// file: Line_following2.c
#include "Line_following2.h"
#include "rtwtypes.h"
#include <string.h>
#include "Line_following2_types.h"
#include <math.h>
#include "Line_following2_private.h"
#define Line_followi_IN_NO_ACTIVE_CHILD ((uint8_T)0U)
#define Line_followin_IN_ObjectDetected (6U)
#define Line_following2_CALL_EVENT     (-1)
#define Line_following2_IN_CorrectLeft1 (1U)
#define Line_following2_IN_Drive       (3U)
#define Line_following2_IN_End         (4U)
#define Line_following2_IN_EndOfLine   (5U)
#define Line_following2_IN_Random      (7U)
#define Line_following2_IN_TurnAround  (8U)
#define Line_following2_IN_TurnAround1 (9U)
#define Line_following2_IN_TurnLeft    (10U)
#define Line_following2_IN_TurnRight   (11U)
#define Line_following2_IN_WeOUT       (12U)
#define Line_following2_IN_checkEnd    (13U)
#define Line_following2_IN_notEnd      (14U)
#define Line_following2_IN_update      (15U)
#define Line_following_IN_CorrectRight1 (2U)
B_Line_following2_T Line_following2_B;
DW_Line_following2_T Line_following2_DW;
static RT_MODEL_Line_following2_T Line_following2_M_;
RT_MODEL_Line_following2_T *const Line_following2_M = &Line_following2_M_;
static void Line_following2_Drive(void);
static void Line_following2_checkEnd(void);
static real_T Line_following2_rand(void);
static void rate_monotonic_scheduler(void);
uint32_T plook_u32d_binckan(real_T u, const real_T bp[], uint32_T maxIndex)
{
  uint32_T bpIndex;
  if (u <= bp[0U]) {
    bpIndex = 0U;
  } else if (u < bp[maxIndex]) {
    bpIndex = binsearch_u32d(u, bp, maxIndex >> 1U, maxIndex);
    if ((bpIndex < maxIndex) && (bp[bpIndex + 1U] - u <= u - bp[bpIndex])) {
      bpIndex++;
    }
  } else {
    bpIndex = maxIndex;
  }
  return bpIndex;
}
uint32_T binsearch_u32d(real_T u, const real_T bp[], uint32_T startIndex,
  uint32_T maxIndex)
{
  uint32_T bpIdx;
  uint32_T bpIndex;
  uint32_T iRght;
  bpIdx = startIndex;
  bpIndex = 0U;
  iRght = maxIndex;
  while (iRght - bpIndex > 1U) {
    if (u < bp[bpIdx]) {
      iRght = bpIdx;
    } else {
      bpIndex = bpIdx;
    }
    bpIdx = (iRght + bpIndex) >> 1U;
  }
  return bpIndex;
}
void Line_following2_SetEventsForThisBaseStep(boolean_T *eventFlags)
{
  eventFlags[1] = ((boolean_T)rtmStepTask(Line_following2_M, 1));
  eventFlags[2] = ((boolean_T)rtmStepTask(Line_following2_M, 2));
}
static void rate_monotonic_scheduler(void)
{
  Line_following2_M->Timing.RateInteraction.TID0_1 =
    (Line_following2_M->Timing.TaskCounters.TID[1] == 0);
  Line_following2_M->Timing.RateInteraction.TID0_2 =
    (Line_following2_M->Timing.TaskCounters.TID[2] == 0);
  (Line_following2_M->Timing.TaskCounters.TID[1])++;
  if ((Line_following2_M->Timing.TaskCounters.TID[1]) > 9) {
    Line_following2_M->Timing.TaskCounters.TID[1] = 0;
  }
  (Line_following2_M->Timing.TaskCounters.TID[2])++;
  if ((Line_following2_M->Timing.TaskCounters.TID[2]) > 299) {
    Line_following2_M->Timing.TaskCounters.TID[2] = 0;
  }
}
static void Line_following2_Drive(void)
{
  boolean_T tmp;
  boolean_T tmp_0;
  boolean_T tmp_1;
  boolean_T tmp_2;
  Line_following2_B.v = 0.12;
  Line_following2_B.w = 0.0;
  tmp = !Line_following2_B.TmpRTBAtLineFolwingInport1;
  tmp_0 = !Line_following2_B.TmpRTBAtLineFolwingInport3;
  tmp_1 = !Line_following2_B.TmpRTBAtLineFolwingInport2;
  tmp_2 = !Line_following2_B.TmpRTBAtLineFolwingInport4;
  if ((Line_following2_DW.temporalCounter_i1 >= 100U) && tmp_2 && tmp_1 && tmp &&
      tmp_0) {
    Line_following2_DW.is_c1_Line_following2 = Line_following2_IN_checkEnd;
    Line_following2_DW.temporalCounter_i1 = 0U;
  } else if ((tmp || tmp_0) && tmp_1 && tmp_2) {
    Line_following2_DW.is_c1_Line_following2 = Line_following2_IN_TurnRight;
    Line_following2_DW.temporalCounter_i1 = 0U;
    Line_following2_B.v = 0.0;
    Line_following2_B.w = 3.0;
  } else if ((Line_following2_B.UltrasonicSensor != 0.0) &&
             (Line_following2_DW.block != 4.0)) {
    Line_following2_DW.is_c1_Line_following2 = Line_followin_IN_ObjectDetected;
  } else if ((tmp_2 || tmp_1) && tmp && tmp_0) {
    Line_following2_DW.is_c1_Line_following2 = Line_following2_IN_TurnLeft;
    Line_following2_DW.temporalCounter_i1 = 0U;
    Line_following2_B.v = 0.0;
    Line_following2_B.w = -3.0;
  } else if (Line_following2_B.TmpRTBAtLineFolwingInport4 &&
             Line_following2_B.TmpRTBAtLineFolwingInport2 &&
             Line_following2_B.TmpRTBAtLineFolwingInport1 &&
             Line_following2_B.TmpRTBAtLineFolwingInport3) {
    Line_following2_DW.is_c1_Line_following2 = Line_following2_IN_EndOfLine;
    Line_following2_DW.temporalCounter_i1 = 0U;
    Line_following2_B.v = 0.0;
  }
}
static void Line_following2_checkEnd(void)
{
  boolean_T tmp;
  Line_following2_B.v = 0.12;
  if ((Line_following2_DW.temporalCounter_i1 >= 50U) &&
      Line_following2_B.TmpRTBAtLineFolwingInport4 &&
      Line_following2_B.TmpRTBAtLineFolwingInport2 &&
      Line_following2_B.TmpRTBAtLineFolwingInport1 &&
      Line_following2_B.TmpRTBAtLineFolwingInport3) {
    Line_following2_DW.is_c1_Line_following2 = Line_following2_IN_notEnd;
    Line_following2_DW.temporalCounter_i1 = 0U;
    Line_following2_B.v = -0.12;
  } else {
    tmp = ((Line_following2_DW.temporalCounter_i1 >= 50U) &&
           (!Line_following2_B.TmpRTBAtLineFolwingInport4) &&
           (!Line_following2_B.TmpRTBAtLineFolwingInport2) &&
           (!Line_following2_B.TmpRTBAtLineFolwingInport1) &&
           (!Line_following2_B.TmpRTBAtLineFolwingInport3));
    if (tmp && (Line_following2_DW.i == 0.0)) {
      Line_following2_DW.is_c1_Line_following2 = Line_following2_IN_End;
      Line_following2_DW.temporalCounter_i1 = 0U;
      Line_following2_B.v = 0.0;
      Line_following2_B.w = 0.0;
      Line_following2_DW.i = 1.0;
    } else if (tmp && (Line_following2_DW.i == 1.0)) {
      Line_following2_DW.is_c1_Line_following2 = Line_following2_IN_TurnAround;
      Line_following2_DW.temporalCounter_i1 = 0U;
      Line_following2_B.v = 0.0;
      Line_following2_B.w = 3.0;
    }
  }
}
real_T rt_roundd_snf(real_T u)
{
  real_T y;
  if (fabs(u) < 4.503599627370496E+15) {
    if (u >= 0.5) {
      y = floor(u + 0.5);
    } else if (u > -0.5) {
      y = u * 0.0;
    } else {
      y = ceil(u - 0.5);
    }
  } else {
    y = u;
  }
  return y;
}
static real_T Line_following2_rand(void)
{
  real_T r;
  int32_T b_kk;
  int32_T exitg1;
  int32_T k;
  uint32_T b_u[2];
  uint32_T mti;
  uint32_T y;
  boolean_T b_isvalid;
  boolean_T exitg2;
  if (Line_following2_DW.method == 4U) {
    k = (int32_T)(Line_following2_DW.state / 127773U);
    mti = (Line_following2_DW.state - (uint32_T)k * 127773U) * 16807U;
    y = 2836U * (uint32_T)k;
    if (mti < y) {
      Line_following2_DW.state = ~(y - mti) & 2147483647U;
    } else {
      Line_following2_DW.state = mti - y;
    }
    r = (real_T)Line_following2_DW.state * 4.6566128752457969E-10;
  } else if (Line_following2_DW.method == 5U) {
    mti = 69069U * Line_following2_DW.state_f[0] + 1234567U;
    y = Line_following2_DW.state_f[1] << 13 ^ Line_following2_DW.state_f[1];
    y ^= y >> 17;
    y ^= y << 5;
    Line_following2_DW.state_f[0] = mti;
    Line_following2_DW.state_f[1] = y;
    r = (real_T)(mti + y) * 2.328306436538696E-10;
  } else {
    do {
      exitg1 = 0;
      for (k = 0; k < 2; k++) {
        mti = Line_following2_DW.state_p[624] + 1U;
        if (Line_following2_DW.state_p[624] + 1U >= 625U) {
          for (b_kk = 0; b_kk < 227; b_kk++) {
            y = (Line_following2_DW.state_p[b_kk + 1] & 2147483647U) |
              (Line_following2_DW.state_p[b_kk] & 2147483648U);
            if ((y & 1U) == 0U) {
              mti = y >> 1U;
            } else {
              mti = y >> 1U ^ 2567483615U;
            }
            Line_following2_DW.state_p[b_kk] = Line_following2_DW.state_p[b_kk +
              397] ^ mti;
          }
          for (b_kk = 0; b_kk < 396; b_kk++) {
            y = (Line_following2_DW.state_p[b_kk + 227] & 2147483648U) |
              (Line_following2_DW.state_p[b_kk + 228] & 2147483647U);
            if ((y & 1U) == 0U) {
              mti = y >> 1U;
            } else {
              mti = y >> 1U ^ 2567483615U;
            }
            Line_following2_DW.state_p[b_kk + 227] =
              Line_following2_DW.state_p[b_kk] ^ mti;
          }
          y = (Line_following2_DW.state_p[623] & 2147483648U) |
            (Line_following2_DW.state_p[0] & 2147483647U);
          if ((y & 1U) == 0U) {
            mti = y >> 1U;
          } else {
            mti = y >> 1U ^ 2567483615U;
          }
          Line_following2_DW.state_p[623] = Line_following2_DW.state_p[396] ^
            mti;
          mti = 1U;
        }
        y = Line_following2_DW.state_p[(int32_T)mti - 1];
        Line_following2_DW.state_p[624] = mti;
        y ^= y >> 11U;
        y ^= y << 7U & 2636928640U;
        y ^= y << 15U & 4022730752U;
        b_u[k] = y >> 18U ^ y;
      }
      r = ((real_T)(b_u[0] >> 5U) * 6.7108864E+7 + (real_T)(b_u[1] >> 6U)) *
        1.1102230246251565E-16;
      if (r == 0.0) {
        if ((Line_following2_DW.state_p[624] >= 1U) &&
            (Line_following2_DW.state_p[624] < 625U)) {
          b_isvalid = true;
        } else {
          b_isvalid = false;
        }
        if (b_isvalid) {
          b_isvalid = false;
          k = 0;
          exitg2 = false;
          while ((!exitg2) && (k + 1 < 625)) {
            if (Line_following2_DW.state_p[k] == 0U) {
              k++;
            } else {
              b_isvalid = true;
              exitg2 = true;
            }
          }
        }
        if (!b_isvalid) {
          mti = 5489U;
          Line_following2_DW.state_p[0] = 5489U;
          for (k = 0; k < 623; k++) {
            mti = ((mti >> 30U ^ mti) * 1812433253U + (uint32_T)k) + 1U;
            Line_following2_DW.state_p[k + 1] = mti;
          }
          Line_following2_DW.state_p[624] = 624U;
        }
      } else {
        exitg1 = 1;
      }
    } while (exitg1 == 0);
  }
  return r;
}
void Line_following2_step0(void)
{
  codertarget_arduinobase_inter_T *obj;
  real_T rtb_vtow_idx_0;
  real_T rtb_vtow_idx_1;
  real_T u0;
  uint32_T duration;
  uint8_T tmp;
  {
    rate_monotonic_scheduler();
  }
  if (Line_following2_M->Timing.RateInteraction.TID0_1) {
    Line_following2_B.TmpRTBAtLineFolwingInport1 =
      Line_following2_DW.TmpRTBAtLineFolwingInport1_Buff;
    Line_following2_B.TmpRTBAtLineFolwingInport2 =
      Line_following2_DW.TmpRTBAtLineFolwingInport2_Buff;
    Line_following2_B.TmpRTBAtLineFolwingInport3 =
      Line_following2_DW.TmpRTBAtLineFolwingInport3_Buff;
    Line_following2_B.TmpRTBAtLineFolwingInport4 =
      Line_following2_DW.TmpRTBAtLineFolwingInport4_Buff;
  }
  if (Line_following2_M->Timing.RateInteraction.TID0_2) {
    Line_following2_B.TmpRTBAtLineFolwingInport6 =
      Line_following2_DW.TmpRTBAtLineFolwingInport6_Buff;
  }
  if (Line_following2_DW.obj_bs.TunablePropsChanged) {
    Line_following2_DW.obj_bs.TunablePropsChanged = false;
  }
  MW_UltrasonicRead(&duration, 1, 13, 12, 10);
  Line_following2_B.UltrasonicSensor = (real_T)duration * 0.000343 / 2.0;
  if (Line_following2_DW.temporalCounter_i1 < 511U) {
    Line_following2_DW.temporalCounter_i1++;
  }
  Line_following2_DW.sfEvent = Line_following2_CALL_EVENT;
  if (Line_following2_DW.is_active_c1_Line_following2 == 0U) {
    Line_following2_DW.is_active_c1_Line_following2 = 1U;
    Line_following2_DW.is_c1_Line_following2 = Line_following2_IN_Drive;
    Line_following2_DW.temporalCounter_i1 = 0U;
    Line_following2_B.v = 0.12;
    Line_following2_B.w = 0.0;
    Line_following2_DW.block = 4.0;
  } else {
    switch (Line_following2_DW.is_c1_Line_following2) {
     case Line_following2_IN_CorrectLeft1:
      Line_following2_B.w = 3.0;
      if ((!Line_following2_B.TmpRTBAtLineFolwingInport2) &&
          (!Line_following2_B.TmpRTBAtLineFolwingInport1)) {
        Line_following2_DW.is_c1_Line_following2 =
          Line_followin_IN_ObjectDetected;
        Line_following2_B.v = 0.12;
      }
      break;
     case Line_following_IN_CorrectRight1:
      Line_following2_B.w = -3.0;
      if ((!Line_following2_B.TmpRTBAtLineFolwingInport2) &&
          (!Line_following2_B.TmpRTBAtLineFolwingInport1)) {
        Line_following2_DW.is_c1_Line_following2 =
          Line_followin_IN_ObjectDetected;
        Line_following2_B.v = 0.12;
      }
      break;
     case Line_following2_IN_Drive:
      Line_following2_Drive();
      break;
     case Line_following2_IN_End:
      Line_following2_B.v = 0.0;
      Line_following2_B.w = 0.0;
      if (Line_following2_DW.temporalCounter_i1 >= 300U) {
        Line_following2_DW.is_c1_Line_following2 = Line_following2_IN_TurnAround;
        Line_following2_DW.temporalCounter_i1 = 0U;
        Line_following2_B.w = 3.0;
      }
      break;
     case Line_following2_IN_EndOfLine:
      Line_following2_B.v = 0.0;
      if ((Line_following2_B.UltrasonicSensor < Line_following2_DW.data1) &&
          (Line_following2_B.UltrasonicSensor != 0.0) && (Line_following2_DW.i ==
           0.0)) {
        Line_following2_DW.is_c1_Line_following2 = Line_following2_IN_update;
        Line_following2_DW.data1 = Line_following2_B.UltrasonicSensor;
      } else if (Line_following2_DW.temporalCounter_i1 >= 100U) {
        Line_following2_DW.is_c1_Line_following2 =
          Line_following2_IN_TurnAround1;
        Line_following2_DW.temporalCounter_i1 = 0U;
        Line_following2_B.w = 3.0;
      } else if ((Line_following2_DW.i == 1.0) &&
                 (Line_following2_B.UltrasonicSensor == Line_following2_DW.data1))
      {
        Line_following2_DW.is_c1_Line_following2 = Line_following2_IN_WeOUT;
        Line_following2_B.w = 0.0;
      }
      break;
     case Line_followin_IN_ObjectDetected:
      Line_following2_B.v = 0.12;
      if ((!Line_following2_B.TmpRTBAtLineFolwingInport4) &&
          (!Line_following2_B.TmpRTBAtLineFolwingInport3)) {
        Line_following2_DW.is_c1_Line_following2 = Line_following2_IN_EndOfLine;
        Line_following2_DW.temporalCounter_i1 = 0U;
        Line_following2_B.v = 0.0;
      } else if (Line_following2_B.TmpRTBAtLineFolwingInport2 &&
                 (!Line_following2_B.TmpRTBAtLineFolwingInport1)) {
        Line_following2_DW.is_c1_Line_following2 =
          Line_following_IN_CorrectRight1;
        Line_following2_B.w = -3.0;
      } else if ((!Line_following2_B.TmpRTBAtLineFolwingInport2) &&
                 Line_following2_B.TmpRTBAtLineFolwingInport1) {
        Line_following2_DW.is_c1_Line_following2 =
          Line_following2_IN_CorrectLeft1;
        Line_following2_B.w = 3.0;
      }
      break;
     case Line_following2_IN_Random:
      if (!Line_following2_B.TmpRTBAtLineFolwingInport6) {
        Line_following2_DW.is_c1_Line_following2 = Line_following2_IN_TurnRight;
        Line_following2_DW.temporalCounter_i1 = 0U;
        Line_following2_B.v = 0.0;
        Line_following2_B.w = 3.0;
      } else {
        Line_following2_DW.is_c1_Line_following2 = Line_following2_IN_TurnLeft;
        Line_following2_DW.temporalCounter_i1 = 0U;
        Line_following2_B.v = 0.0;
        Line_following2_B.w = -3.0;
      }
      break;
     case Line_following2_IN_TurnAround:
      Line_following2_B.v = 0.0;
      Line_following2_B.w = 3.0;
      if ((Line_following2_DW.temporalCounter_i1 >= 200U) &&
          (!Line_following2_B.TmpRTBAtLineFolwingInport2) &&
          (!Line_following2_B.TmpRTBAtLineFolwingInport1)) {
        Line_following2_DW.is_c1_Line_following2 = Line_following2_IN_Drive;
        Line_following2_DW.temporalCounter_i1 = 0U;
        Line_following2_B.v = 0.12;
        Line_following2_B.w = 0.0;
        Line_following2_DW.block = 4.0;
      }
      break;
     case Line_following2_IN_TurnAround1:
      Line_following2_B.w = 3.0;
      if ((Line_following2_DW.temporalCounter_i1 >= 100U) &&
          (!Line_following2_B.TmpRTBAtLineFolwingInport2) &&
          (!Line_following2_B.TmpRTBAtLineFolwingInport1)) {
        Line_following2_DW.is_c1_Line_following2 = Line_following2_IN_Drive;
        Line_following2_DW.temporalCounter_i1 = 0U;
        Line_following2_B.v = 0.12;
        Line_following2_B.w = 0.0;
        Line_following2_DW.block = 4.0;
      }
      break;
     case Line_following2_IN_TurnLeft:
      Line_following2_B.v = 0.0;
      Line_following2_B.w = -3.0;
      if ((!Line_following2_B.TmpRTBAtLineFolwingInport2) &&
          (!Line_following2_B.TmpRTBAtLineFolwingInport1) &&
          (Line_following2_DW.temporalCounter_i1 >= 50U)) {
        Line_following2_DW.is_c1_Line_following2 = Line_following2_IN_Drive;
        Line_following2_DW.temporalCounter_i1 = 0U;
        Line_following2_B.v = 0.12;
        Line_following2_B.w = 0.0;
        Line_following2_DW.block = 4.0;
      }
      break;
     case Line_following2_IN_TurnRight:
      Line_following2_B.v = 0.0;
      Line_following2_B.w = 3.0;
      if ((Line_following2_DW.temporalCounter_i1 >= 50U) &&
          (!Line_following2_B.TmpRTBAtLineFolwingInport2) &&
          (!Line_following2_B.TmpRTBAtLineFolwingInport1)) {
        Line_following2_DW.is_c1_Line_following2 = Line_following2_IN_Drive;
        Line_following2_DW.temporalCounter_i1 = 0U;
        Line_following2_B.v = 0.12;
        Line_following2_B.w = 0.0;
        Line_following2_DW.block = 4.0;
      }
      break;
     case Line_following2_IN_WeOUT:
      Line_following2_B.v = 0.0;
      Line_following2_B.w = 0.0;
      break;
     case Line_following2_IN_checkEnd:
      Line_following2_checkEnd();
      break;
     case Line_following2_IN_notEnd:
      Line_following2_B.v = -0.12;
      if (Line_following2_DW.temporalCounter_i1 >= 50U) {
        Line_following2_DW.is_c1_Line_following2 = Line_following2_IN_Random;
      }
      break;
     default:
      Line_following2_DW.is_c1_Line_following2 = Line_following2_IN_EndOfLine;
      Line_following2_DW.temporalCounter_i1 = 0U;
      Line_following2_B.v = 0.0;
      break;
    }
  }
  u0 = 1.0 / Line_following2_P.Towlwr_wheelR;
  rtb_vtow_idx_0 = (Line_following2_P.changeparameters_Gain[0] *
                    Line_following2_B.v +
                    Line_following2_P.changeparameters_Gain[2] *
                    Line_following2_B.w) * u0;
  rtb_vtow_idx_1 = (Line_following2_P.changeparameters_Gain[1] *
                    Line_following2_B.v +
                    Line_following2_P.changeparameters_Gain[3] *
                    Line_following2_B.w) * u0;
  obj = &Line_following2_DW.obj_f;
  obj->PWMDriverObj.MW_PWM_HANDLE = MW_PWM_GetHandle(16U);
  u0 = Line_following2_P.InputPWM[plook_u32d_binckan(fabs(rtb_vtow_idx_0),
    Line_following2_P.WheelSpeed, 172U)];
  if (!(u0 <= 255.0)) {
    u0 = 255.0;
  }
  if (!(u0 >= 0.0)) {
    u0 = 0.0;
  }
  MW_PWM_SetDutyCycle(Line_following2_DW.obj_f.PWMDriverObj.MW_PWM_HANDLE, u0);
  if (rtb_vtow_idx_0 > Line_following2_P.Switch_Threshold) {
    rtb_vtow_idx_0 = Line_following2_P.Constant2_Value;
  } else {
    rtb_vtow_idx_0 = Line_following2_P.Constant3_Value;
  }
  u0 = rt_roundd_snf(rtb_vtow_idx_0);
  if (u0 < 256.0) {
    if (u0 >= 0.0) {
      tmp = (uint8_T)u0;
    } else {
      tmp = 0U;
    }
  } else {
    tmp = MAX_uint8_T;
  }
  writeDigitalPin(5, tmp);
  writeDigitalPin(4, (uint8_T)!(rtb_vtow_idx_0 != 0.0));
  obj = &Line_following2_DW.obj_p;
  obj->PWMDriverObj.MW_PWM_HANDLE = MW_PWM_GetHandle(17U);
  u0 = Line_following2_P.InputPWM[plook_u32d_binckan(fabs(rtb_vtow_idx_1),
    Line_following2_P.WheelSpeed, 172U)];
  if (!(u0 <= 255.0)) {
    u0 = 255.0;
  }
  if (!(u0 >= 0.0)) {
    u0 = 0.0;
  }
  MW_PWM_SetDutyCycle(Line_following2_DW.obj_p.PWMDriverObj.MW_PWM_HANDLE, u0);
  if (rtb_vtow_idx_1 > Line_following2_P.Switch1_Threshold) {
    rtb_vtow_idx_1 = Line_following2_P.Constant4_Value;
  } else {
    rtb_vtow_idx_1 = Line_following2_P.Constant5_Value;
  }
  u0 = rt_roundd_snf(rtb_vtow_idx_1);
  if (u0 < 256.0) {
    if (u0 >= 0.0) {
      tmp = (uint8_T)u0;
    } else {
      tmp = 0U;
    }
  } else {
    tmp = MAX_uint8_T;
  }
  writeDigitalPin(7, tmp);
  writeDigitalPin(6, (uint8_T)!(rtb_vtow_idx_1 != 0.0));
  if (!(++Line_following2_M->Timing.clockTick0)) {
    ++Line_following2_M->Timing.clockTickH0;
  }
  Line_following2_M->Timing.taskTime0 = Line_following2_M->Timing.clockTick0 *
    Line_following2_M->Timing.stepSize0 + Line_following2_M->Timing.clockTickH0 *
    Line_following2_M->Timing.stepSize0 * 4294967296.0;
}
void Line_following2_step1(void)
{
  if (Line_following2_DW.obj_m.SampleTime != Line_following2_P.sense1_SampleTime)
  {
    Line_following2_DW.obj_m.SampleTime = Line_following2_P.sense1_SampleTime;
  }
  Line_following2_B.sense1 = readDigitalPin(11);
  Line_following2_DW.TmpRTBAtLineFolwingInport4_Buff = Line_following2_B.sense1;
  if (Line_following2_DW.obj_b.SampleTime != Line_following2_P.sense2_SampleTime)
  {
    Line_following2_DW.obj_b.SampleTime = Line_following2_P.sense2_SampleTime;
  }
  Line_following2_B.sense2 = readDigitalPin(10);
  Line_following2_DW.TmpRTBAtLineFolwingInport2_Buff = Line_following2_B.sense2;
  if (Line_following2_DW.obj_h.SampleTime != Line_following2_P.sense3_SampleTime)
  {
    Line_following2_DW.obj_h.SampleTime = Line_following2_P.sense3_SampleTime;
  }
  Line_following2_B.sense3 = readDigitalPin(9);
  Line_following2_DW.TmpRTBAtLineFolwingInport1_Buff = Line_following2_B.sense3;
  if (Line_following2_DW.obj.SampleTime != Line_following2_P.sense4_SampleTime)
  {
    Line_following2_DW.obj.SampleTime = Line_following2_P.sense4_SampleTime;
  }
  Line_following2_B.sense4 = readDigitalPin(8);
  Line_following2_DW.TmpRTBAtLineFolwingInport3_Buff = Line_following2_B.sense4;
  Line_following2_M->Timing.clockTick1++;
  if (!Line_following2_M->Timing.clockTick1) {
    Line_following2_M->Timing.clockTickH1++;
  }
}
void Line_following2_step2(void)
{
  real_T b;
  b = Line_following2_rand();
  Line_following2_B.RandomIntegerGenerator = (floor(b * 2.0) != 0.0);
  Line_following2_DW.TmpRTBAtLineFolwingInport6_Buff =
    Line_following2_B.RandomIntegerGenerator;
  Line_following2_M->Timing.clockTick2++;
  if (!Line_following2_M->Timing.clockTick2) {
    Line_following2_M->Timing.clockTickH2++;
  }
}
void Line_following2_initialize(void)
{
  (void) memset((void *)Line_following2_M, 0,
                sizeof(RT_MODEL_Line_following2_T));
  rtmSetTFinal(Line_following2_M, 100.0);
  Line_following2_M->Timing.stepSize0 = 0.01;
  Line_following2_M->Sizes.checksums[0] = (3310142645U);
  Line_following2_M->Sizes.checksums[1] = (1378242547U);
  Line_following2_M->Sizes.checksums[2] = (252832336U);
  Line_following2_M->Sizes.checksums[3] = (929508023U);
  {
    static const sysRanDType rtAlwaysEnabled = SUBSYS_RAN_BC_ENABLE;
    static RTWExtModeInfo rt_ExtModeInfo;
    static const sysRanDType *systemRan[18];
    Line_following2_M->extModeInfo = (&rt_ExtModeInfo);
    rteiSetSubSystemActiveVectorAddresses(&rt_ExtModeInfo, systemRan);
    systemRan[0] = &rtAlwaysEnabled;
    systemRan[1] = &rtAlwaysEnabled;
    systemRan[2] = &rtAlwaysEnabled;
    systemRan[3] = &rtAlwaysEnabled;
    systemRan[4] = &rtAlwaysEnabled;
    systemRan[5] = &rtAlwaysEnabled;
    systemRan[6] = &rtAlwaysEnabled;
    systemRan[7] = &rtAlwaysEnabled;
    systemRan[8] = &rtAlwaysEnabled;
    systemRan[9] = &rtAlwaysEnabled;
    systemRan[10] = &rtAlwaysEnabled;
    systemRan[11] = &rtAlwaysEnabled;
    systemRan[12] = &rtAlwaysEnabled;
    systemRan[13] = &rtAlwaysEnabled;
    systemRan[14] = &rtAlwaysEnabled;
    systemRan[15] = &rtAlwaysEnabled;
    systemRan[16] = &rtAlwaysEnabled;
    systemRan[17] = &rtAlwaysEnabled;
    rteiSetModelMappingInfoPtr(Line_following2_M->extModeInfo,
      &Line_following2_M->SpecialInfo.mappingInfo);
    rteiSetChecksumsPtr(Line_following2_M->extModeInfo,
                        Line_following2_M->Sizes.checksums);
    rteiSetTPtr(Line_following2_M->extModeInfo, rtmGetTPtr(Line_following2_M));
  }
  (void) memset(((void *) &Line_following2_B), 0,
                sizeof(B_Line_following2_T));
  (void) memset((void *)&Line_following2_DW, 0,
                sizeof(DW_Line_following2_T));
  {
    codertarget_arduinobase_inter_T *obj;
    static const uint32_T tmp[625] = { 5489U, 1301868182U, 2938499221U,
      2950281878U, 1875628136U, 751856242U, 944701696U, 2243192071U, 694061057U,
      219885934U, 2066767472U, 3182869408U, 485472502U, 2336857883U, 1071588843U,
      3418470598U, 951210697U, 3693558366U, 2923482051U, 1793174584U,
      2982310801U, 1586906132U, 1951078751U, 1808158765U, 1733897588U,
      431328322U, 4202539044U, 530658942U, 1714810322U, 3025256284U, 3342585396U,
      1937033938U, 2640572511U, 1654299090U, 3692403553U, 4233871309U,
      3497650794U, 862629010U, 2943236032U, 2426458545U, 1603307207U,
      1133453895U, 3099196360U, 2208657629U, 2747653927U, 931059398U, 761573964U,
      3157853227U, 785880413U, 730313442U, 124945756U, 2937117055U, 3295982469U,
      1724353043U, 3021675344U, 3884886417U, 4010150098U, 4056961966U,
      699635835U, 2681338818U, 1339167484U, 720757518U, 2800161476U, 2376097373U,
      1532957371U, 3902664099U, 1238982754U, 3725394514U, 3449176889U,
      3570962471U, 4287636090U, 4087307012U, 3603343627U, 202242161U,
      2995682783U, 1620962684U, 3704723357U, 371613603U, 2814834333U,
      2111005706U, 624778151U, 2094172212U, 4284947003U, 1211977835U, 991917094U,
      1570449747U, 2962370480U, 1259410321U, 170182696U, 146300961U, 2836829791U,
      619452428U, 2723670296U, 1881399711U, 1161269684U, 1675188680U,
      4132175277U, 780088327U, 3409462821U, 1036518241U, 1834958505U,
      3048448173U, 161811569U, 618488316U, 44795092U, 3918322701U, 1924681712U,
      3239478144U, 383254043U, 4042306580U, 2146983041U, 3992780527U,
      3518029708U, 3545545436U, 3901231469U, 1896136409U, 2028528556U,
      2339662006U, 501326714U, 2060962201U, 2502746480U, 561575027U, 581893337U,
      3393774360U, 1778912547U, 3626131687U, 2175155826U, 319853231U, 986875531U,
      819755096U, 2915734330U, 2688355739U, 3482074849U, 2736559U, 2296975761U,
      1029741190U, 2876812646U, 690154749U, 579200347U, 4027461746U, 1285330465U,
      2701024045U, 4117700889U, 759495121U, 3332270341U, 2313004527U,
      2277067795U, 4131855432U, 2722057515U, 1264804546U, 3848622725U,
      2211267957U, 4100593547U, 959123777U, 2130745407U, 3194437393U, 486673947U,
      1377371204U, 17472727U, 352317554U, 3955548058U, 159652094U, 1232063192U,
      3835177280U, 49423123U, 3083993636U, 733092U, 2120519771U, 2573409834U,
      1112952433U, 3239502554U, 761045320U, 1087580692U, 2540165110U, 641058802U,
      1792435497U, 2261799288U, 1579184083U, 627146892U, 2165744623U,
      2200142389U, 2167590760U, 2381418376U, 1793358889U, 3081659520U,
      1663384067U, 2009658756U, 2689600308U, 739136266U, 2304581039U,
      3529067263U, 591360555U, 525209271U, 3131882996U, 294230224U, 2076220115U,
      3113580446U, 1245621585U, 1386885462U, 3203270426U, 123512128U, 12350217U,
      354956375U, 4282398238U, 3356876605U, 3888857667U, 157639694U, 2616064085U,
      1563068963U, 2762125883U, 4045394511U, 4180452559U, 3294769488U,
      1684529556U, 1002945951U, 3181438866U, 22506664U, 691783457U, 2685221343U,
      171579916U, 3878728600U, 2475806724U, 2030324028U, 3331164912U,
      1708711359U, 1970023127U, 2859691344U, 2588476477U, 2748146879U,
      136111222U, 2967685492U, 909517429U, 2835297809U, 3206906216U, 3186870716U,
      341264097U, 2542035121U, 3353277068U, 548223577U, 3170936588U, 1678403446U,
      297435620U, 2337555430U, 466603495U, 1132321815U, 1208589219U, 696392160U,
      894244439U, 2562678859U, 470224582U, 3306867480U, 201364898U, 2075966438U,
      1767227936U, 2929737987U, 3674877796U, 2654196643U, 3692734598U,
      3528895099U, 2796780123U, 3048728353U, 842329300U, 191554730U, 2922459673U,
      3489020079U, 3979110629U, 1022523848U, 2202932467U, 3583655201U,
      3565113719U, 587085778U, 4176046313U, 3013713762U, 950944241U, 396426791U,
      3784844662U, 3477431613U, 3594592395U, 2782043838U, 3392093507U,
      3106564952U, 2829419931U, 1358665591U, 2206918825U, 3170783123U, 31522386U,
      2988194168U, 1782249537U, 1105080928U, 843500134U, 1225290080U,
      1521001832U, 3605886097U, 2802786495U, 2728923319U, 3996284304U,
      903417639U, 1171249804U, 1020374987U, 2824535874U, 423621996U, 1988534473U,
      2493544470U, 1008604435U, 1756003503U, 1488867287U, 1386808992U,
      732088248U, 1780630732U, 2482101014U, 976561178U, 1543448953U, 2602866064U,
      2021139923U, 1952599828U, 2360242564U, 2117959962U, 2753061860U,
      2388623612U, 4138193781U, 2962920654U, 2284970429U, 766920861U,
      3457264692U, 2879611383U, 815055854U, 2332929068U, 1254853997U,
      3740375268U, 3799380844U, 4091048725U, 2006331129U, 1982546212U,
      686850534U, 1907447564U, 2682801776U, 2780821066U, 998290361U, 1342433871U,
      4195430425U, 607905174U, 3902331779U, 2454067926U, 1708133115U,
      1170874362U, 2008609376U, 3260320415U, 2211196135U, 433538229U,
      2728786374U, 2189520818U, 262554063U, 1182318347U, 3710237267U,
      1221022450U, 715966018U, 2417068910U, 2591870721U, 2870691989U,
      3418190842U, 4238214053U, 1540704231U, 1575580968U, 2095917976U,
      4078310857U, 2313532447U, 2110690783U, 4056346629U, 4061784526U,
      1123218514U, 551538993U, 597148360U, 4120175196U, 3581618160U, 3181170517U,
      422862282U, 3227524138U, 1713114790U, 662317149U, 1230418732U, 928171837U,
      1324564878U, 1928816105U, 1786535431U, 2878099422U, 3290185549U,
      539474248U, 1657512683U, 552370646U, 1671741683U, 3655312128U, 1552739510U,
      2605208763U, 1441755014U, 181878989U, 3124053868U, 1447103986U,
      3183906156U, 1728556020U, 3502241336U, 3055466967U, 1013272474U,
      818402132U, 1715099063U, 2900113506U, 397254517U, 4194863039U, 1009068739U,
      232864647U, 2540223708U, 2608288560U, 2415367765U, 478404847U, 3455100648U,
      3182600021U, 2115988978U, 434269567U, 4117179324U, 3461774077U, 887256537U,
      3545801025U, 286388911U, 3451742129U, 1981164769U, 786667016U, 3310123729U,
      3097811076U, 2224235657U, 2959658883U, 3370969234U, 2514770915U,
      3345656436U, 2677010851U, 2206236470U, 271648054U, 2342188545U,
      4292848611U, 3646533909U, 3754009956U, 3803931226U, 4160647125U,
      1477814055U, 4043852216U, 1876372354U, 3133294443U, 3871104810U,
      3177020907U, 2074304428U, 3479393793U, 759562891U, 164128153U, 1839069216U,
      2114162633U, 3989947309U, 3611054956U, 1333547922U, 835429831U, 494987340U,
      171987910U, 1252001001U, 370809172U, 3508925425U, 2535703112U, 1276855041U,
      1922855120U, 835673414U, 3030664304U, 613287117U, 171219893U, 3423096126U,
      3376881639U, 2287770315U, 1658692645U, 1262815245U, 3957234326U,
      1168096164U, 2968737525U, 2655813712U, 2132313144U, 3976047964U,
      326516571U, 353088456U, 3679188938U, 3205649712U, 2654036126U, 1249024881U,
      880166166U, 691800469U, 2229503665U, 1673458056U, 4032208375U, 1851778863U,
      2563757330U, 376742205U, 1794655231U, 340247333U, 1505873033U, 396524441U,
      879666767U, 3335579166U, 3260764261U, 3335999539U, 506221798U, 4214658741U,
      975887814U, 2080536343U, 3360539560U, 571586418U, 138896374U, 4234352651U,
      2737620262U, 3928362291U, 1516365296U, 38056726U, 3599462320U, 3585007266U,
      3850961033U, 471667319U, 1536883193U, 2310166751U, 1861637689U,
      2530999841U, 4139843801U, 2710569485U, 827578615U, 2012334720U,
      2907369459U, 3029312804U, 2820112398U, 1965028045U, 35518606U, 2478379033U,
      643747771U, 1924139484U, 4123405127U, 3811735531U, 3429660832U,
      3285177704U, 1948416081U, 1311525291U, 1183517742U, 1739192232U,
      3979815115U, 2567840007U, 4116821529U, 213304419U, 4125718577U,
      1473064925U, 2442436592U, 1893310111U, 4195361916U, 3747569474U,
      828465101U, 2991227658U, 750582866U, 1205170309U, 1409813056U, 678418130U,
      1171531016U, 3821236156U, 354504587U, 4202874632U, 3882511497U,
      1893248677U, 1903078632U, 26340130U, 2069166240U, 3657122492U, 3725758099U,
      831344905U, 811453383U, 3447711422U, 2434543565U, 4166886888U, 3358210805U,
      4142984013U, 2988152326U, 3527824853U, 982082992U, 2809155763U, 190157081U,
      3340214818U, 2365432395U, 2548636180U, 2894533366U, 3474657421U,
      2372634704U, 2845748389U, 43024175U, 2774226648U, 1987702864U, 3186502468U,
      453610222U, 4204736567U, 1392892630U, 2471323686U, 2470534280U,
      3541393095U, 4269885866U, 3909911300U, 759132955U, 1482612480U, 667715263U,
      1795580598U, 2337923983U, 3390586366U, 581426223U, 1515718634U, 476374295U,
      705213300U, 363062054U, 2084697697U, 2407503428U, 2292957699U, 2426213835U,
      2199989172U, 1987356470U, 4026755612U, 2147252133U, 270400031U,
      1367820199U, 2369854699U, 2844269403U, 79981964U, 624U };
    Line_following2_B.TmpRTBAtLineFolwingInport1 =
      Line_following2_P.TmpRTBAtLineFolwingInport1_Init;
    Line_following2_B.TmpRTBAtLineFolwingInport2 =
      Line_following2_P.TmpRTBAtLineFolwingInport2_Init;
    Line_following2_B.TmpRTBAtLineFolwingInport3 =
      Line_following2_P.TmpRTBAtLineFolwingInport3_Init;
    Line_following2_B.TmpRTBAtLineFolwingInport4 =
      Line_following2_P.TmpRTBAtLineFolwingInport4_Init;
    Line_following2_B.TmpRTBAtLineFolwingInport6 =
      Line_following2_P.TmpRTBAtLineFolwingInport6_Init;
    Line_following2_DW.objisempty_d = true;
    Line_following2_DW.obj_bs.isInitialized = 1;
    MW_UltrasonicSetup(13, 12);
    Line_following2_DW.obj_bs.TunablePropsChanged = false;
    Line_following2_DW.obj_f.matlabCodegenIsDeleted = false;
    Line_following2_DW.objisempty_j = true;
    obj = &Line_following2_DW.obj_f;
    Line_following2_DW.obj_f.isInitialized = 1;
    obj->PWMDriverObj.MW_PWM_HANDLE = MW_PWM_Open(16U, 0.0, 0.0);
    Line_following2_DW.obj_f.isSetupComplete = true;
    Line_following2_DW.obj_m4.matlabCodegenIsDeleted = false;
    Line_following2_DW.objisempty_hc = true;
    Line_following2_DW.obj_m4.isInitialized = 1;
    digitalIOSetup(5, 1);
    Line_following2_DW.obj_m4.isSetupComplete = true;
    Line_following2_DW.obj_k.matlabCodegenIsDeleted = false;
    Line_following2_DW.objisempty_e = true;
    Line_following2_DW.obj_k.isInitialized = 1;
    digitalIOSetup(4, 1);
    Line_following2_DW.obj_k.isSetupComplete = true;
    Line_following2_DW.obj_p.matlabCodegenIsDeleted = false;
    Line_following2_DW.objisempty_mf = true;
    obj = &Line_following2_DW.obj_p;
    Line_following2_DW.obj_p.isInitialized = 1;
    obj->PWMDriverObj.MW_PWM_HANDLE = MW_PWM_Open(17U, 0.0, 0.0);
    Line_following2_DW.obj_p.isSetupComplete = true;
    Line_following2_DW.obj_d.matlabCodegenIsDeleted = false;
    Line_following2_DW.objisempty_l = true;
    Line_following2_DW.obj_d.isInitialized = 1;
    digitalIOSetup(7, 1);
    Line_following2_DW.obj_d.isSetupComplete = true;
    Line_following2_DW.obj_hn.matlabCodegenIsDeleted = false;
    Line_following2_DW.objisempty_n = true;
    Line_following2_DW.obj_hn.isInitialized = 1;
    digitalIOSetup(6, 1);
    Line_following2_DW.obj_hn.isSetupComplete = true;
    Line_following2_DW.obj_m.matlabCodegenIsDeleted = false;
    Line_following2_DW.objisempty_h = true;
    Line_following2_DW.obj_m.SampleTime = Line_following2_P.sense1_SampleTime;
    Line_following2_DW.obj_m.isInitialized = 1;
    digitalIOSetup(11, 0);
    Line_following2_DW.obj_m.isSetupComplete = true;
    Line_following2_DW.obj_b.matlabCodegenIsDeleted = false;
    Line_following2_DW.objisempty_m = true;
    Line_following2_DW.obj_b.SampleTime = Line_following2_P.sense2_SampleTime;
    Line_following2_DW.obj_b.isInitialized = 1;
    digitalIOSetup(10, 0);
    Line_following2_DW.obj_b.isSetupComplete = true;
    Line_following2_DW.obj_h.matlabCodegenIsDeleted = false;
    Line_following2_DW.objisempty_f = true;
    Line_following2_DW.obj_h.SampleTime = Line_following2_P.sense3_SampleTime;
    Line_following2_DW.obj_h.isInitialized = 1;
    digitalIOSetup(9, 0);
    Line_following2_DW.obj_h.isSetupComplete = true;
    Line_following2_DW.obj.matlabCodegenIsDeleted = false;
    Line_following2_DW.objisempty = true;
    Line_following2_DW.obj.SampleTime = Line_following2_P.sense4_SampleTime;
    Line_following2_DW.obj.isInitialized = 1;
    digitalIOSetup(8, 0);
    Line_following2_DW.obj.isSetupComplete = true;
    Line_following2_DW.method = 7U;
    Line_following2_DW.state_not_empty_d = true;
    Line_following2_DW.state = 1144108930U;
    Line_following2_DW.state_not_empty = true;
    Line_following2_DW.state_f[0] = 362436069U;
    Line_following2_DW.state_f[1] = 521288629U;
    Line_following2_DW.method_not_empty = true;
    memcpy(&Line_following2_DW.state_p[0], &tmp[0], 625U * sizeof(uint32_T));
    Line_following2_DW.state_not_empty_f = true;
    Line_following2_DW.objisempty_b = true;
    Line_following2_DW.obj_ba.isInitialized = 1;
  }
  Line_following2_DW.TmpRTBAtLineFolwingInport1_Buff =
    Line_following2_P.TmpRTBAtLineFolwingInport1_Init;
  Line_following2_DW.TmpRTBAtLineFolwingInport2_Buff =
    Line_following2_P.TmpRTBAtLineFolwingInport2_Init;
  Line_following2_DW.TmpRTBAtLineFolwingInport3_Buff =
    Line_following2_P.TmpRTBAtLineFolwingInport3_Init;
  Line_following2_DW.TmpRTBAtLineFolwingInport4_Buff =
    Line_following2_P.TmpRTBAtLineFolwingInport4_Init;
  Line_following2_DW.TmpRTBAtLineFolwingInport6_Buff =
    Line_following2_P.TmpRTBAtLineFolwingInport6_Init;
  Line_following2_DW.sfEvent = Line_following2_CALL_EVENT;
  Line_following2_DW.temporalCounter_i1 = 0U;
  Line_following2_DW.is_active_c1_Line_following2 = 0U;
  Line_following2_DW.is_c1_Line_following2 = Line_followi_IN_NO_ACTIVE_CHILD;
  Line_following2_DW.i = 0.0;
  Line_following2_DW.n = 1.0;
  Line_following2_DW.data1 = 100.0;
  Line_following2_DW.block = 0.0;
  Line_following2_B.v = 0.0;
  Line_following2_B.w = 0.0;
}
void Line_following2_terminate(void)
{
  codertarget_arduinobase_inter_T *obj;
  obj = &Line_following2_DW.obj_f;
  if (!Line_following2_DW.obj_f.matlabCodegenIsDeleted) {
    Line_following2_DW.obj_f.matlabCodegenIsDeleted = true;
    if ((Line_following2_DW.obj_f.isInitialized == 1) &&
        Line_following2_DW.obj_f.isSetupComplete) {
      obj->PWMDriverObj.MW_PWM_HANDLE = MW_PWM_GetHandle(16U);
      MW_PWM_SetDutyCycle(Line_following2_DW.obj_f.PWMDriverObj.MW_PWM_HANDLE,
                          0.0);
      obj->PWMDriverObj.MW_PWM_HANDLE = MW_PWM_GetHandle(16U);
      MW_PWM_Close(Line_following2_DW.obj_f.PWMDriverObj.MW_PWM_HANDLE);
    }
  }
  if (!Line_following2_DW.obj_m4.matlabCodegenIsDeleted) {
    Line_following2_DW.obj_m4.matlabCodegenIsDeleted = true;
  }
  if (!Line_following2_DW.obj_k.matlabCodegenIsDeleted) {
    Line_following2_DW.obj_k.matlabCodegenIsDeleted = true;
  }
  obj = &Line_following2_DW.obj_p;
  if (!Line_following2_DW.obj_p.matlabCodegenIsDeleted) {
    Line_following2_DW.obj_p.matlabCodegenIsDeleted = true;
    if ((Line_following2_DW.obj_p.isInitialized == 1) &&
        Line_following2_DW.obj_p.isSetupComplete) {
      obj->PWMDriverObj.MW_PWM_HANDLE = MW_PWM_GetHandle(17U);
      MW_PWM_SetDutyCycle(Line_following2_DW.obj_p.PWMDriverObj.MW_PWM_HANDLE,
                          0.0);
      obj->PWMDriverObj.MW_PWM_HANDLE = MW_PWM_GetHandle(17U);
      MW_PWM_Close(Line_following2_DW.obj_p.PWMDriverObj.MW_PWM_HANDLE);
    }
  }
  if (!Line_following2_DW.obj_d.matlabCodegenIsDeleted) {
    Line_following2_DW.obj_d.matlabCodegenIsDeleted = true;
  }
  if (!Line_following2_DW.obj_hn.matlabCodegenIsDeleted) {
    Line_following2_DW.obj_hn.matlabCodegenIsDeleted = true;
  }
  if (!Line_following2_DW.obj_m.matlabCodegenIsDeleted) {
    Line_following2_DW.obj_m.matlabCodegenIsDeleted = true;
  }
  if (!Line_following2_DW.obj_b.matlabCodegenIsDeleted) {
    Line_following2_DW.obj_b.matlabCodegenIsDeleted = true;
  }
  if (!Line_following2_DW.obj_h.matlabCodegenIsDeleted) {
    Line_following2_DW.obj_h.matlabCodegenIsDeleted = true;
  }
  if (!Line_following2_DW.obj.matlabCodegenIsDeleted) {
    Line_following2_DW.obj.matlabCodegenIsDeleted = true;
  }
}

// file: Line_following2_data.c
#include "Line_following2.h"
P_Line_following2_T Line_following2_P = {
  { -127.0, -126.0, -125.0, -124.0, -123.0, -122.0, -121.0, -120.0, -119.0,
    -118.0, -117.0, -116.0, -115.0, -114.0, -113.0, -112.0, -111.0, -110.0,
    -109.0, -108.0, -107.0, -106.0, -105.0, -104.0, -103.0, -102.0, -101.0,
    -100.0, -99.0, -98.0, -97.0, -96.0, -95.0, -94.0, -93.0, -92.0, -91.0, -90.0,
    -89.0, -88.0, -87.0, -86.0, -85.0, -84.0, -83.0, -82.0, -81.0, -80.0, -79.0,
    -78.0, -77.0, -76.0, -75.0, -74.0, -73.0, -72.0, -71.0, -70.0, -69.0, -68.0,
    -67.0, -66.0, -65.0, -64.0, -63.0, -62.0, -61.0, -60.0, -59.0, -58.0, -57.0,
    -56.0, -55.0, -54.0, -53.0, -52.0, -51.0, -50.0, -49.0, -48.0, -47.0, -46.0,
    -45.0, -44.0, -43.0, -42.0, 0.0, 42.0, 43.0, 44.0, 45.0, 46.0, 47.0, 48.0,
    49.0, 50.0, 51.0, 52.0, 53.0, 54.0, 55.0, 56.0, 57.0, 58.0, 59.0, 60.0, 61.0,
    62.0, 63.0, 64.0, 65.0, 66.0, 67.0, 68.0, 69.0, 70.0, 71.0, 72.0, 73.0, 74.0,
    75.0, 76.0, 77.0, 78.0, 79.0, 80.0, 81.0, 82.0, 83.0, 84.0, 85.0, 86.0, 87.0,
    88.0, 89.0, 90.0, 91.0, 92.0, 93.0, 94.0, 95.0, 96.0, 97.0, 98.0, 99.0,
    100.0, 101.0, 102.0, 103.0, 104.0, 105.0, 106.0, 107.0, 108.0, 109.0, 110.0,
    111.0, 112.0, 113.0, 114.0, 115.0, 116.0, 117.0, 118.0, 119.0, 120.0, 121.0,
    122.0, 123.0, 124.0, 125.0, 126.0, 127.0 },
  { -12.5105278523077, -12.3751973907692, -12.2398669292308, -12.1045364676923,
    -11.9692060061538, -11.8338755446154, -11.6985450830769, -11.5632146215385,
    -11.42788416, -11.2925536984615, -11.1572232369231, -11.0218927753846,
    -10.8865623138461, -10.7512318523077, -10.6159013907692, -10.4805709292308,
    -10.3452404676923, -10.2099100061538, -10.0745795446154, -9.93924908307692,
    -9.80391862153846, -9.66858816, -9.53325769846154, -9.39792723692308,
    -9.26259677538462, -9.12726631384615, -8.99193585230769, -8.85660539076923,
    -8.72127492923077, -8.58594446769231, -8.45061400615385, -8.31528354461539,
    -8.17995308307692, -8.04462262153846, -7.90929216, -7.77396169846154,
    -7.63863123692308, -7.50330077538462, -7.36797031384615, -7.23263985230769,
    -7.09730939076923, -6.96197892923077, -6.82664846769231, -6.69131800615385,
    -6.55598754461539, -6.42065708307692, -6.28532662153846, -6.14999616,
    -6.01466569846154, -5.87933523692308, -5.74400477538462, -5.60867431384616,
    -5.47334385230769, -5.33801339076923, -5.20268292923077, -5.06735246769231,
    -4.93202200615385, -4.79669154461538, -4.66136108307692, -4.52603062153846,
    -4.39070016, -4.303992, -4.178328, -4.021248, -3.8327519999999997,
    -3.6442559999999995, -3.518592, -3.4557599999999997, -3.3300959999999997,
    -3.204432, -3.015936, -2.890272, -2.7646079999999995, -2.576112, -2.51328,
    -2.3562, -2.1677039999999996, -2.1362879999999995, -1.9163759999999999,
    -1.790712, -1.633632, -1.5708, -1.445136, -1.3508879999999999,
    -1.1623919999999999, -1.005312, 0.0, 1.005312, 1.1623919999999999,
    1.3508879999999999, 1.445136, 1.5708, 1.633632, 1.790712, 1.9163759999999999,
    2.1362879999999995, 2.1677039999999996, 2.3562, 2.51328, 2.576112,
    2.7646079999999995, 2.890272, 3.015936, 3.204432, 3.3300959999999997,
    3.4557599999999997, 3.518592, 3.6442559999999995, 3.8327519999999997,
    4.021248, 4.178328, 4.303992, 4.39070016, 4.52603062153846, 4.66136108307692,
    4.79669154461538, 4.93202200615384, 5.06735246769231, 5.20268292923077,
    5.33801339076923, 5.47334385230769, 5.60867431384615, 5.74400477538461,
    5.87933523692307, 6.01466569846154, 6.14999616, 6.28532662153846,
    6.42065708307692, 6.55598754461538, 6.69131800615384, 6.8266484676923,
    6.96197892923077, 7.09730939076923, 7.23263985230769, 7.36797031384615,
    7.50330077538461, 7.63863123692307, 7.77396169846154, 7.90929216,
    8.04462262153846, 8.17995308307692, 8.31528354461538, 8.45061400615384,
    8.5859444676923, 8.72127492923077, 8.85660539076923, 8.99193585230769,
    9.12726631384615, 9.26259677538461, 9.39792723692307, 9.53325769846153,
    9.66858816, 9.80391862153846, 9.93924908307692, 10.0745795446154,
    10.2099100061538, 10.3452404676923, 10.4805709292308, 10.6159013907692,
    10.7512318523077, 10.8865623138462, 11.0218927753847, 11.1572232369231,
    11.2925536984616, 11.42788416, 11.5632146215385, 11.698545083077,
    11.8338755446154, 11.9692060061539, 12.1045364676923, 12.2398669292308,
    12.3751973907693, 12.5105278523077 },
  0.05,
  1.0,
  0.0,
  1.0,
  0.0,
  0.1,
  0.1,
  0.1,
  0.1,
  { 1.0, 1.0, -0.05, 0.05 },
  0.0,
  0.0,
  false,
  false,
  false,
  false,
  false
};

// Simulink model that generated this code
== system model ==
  PWM#1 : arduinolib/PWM  pinNumber=16  <- 1: Lookup_nD#1
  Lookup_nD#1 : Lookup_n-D  BreakpointsForDimension1=WheelSpeed  Table=InputPWM  InterpMethod=Nearest  <- 1: Abs#1
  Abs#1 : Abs  <- 1: Towlwr
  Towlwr : mobileRoboticsTrainingLib/To wlwr  <- 1: Stateflowchart#1, 2: Stateflowchart#1/2
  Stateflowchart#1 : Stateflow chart  <- 1: sense3, 2: sense2, 3: sense4, 4: sense1, 5: UltrasonicSensor, 6: RandomIntegerGenerator
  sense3 : arduinolib/Digital Input  pinNumber=9
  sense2 : arduinolib/Digital Input  pinNumber=10
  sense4 : arduinolib/Digital Input  pinNumber=8
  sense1 : arduinolib/Digital Input  pinNumber=11
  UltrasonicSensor : arduinosensorlib/Ultrasonic Sensor
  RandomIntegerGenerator : commrandsrc3/Random Integer Generator
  DigitalOutput#1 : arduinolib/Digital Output  pinNumber=5  <- 1: Switch
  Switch : Switch  Criteria=u2 > Threshold  <- 1: Constant2, 2: Towlwr, 3: Constant3
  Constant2 : Constant
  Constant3 : Constant  Value=0
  DigitalOutput#2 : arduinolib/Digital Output  pinNumber=4  <- 1: Logic#1
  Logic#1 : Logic  Operator=NOT  <- 1: Switch
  PWM#2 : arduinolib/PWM  pinNumber=17  <- 1: Lookup_nD#2
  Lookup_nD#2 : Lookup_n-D  BreakpointsForDimension1=WheelSpeed  Table=InputPWM  InterpMethod=Nearest  <- 1: Abs#2
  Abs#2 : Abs  <- 1: Towlwr/2
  DigitalOutput#3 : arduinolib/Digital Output  pinNumber=7  <- 1: Switch1
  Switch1 : Switch  Criteria=u2 > Threshold  <- 1: Constant4, 2: Towlwr/2, 3: Constant5
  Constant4 : Constant
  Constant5 : Constant  Value=0
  DigitalOutput#4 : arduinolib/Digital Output  pinNumber=6  <- 1: Logic#2
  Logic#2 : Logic  Operator=NOT  <- 1: Switch1
== stateflow chart Stateflowchart#1 ==
  state Random
    entry:
    dir;
  state notEnd
    entry:
    v=-0.12;
  state End
    entry:
    v=0;
    w=0;
    i=1;
  state TurnAround
    entry:
    v=0;
    w=3;
  state checkEnd
    entry:
    v=0.12;
  state TurnLeft
    entry:
    v=0;
    w=-3;
  state TurnRight
    entry:
    v=0;
    w=3;
  state Drive
    entry:
    v=0.12;
    w=0;
    i;
    n;
    data1;
    block=4;
  state ObjectDetected
    entry:
    v=0.12;
  state CorrectRight1
    entry:
    w=-3;
  state TurnAround1
    entry:
    w=3;
  state CorrectLeft1
    entry:
    w=3;
  state EndOfLine
    entry:
    v=0;
  state update
    entry:
    data1=ultraSonic;
  state WeOUT
    entry:
    v=0;
    w=0;
  checkEnd -> TurnAround [order 3] : [after(0.5,sec) &&sense1 ==0 && sense2 == 0 && sense3 ==0 && sense4==0 && i==1]
  Random -> TurnLeft [order 2] : [dir==1]
  Random -> TurnRight [order 1] : [dir==0]
  notEnd -> Random : [after(0.5,sec)]
  checkEnd -> notEnd [order 1] : [after(0.5,sec) &&sense1 == 1 && sense2 == 1 && sense3 ==1 && sense4==1 ]
  End -> TurnAround : [after(3,sec)]
  checkEnd -> End [order 2] : [after(0.5,sec) &&sense1 ==0 && sense2 == 0 && sense3 ==0 && sense4==0 && i==0]
  TurnAround -> Drive : [after(2,sec) && sense2 == 0 && sense3 == 0]
  Drive -> checkEnd [order 1] : [after(1,sec) && sense1 == 0 && sense2 == 0 && sense3 == 0 && sense4==0]
  (default) -> Drive
  TurnRight -> Drive : [after(0.5,sec) && sense2 ==0 && sense3 ==0]
  Drive -> TurnLeft [order 4] : [ sense1 == 0 | sense2 == 0 && sense3 == 0  && sense4==0]
  TurnLeft -> Drive : [sense2==0 && sense3==0 && after(0.5,sec)]
  Drive -> TurnRight [order 2] : [sense3 == 0 | sense4==0 && sense2 == 0 && sense1 == 0 ]
  TurnAround1 -> Drive : [after(1,sec) && sense2 == 0 && sense3 == 0]
  Drive -> EndOfLine [order 5] : [sense1 == 1 && sense2 == 1 && sense3 == 1 && sense4==1]
  Drive -> ObjectDetected [order 3] : [ultraSonic ~= 0 && block~=4]
  ObjectDetected -> CorrectRight1 [order 2] : [sense2==1 && sense3 ==0]
  ObjectDetected -> CorrectLeft1 [order 3] : [sense2==0 && sense3 ==1]
  CorrectRight1 -> ObjectDetected : [sense2==0 && sense3 == 0]
  CorrectLeft1 -> ObjectDetected : [sense2 ==0 && sense3 ==0]
  ObjectDetected -> EndOfLine [order 1] : [sense1 == 0 && sense4 == 0]
  EndOfLine -> TurnAround1 [order 2] : [after(1,sec)]
  update -> EndOfLine
  EndOfLine -> update [order 1] : [ultraSonic<data1 && ultraSonic~=0 && i==0]
  EndOfLine -> WeOUT [order 3] : [i==1 && ultraSonic==data1]
  data: v output; w output; sense3 input; sense2 input; sense4 input; sense1 input; ultraSonic input; i local =0; dir input; n local =1; data1 local =100; block local
